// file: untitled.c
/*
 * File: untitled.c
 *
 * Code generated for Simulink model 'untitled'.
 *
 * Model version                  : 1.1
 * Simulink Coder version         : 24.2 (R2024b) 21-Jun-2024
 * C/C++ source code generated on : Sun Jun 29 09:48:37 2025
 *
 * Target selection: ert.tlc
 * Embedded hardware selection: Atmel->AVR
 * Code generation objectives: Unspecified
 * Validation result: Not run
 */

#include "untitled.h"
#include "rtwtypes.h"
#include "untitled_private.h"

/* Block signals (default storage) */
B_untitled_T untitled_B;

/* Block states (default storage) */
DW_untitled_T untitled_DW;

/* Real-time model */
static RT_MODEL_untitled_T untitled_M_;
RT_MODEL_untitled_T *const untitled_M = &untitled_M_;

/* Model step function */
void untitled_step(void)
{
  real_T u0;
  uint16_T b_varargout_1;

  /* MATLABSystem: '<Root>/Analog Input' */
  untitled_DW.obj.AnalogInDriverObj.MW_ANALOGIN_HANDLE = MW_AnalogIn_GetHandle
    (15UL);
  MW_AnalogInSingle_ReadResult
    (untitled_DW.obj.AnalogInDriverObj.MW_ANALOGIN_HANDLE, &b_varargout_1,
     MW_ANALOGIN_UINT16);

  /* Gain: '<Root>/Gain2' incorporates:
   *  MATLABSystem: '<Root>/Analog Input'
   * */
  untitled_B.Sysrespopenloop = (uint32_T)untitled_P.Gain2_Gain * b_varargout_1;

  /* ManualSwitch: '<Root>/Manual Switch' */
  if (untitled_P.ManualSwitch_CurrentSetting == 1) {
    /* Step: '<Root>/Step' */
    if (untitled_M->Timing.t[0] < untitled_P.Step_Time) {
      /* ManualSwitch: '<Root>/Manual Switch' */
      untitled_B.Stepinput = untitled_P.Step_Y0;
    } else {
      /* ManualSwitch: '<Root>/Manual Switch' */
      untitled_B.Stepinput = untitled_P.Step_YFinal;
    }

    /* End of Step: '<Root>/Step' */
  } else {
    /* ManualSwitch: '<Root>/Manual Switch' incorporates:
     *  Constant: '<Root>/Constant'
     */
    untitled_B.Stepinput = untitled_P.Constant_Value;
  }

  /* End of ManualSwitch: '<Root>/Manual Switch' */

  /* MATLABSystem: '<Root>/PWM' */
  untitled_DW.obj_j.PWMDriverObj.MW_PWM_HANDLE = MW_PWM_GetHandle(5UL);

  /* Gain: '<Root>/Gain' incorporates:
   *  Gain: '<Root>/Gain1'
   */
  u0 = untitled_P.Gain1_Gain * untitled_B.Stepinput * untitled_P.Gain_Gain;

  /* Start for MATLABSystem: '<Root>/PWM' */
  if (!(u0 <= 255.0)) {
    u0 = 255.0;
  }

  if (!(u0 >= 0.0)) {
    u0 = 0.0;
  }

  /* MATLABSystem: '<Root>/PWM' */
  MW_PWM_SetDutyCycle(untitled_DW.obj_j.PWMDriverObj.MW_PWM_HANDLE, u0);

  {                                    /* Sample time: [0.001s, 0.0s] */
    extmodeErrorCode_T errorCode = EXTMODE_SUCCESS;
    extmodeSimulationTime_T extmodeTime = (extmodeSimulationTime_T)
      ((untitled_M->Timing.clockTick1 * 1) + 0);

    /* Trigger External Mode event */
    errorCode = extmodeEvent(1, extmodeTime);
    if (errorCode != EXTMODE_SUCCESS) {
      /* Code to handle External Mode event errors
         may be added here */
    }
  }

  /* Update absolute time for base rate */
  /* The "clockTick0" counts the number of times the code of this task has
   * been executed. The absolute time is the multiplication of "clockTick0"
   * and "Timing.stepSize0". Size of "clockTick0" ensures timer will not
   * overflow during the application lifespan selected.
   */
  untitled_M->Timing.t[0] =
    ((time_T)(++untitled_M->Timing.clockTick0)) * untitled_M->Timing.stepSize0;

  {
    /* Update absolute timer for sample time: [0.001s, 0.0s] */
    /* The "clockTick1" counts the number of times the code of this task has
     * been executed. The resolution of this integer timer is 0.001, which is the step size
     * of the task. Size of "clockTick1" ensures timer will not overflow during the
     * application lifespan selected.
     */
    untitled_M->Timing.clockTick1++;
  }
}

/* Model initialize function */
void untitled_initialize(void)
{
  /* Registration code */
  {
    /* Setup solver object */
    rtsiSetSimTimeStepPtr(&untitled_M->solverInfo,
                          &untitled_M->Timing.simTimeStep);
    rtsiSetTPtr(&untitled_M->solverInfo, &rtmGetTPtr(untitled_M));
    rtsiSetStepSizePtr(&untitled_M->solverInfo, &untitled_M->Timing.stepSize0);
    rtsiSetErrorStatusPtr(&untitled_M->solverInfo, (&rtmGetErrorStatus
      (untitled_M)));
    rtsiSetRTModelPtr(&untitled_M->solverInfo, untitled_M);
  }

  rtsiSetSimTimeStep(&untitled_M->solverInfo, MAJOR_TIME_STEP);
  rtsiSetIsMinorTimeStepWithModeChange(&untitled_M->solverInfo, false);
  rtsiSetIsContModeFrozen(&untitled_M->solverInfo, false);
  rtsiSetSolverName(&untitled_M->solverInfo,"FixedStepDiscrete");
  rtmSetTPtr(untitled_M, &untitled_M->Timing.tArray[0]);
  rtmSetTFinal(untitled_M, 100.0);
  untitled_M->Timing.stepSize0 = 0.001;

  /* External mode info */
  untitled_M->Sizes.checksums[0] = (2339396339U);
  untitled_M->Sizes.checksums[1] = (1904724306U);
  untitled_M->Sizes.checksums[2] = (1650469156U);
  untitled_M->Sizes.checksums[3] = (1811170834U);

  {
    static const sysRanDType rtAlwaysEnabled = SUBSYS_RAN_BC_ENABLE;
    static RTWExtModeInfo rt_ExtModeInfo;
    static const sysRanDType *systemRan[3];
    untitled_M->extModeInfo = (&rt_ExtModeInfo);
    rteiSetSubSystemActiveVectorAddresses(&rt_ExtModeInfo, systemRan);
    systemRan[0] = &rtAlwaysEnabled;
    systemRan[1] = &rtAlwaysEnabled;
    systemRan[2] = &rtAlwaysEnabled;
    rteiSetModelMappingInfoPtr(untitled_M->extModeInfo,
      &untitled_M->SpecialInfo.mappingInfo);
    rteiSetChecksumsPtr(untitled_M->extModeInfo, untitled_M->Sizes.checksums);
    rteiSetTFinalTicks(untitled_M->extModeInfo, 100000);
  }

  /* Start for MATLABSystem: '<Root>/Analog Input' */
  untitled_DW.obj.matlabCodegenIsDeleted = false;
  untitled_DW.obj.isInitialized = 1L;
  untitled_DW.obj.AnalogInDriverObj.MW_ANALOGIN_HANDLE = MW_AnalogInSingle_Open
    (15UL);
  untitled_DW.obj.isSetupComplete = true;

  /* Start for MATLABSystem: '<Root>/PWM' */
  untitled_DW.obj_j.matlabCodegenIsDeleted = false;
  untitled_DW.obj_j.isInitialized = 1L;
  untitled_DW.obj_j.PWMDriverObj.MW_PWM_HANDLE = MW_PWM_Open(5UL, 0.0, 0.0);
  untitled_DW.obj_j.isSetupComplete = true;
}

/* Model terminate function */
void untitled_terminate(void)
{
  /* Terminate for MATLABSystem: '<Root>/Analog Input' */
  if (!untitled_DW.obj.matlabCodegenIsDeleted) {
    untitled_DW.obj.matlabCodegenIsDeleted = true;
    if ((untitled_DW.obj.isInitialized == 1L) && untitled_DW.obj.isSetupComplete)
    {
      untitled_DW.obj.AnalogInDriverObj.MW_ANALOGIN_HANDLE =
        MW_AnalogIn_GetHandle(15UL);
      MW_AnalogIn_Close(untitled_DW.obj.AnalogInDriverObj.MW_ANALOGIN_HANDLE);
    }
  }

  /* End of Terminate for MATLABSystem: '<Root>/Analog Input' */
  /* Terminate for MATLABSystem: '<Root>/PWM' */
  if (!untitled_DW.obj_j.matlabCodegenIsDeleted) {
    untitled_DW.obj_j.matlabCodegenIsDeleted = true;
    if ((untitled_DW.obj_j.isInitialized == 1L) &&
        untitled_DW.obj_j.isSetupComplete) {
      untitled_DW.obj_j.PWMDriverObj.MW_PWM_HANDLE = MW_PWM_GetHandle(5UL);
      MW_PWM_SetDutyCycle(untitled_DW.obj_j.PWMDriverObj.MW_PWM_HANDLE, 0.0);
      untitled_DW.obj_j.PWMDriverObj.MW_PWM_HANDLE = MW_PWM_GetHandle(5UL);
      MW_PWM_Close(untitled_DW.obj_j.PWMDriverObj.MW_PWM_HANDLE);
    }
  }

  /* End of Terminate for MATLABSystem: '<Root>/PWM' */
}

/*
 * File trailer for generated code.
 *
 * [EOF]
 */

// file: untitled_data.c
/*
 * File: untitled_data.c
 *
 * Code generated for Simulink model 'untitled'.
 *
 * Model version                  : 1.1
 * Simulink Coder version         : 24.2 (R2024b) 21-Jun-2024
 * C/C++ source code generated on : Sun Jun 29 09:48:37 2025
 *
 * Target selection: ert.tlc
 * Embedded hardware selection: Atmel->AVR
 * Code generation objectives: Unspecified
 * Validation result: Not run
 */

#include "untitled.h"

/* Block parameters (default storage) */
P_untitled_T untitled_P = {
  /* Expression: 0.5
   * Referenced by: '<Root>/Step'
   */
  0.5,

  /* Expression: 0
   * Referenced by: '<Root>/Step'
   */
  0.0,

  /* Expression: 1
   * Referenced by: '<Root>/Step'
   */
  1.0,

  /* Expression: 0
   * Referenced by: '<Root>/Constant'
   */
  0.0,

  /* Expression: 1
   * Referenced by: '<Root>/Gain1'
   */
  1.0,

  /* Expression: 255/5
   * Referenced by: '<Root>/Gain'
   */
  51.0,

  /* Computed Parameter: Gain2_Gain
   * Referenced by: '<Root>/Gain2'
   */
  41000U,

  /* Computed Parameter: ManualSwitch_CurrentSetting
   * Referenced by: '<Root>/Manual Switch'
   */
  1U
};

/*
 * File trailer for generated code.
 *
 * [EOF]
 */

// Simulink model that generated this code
simulink model "untitled"  (R2024b)
settings: Solver=FixedStepAuto  StartTime=0.0  StopTime=100  FixedStep=0.001  RelTol=1e-3  EnableMultiTasking=on
libraries: arduinolib x4

== system untitled ==
  note: Abdulla Mohamed Ibrahem
      | PID Controller Design Module
      | Video (101)
      | OS Academy
  Analog Input : arduinolib/Analog Input  pinNumber=1  ReadResultsOnly=off  ConversionTriggerSource=Software  ExternalTriggerType=uint32( 0 )  OutputDataType=uint16  EnableConversionCompleteNotify=off  EnableOuputStatus=off  SampleTime=-1  blockPlatform=arduino
  Analog Input1 : arduinolib/Analog Input  Commented=on  pinNumber=0  ReadResultsOnly=off  ConversionTriggerSource=Software  ExternalTriggerType=uint32( 0 )  OutputDataType=uint16  EnableConversionCompleteNotify=off  EnableOuputStatus=off  SampleTime=-1  blockPlatform=arduino
  Constant : Constant  Value=0
  Constant1 : Constant  Commented=on  Value=0
  Gain : Gain  Gain=255/5
  Gain1 : Gain
  Gain2 : Gain  Gain=5/1023
  Gain3 : Gain  Commented=on  Gain=255/5
  Gain4 : Gain  Commented=on
  Gain5 : Gain  Commented=on  Gain=5/1023
  Manual Switch : ManualSwitch
  Manual Switch1 : ManualSwitch  Commented=on
  PWM : arduinolib/PWM  pinNumber=5  frequencyType=Default  desiredFrequency=490.2  achievableFrequency=490.2
  PWM1 : arduinolib/PWM  Commented=on  pinNumber=6  frequencyType=Default  desiredFrequency=490.2  achievableFrequency=490.2
  Step : Step  Time=0.5  SampleTime=0
  Step1 : Step  Commented=on  Time=2  SampleTime=0
  Sum : Sum  Commented=on  Inputs=|+-
  Terminator : Terminator
  wires:
  Gain/1 -> PWM/1
  Gain1/1 -> Gain/1
  Analog Input/1 -> Gain2/1
  Constant/1 -> Manual Switch/2
  Step/1 -> Manual Switch/1
  Manual Switch/1 -> Gain1/1  "Step input"
  Gain2/1 -> Terminator/1  "Sys. resp. \"open loop\""
  Step1/1 -> Manual Switch1/1
  Constant1/1 -> Manual Switch1/2
  Analog Input1/1 -> Gain5/1
  Gain4/1 -> Gain3/1
  Gain3/1 -> PWM1/1
  Manual Switch1/1 -> Sum/1  "Step input"
  Sum/1 -> Gain4/1
  Gain5/1 -> Sum/2  "Sys. resp. \"closed loop\""
